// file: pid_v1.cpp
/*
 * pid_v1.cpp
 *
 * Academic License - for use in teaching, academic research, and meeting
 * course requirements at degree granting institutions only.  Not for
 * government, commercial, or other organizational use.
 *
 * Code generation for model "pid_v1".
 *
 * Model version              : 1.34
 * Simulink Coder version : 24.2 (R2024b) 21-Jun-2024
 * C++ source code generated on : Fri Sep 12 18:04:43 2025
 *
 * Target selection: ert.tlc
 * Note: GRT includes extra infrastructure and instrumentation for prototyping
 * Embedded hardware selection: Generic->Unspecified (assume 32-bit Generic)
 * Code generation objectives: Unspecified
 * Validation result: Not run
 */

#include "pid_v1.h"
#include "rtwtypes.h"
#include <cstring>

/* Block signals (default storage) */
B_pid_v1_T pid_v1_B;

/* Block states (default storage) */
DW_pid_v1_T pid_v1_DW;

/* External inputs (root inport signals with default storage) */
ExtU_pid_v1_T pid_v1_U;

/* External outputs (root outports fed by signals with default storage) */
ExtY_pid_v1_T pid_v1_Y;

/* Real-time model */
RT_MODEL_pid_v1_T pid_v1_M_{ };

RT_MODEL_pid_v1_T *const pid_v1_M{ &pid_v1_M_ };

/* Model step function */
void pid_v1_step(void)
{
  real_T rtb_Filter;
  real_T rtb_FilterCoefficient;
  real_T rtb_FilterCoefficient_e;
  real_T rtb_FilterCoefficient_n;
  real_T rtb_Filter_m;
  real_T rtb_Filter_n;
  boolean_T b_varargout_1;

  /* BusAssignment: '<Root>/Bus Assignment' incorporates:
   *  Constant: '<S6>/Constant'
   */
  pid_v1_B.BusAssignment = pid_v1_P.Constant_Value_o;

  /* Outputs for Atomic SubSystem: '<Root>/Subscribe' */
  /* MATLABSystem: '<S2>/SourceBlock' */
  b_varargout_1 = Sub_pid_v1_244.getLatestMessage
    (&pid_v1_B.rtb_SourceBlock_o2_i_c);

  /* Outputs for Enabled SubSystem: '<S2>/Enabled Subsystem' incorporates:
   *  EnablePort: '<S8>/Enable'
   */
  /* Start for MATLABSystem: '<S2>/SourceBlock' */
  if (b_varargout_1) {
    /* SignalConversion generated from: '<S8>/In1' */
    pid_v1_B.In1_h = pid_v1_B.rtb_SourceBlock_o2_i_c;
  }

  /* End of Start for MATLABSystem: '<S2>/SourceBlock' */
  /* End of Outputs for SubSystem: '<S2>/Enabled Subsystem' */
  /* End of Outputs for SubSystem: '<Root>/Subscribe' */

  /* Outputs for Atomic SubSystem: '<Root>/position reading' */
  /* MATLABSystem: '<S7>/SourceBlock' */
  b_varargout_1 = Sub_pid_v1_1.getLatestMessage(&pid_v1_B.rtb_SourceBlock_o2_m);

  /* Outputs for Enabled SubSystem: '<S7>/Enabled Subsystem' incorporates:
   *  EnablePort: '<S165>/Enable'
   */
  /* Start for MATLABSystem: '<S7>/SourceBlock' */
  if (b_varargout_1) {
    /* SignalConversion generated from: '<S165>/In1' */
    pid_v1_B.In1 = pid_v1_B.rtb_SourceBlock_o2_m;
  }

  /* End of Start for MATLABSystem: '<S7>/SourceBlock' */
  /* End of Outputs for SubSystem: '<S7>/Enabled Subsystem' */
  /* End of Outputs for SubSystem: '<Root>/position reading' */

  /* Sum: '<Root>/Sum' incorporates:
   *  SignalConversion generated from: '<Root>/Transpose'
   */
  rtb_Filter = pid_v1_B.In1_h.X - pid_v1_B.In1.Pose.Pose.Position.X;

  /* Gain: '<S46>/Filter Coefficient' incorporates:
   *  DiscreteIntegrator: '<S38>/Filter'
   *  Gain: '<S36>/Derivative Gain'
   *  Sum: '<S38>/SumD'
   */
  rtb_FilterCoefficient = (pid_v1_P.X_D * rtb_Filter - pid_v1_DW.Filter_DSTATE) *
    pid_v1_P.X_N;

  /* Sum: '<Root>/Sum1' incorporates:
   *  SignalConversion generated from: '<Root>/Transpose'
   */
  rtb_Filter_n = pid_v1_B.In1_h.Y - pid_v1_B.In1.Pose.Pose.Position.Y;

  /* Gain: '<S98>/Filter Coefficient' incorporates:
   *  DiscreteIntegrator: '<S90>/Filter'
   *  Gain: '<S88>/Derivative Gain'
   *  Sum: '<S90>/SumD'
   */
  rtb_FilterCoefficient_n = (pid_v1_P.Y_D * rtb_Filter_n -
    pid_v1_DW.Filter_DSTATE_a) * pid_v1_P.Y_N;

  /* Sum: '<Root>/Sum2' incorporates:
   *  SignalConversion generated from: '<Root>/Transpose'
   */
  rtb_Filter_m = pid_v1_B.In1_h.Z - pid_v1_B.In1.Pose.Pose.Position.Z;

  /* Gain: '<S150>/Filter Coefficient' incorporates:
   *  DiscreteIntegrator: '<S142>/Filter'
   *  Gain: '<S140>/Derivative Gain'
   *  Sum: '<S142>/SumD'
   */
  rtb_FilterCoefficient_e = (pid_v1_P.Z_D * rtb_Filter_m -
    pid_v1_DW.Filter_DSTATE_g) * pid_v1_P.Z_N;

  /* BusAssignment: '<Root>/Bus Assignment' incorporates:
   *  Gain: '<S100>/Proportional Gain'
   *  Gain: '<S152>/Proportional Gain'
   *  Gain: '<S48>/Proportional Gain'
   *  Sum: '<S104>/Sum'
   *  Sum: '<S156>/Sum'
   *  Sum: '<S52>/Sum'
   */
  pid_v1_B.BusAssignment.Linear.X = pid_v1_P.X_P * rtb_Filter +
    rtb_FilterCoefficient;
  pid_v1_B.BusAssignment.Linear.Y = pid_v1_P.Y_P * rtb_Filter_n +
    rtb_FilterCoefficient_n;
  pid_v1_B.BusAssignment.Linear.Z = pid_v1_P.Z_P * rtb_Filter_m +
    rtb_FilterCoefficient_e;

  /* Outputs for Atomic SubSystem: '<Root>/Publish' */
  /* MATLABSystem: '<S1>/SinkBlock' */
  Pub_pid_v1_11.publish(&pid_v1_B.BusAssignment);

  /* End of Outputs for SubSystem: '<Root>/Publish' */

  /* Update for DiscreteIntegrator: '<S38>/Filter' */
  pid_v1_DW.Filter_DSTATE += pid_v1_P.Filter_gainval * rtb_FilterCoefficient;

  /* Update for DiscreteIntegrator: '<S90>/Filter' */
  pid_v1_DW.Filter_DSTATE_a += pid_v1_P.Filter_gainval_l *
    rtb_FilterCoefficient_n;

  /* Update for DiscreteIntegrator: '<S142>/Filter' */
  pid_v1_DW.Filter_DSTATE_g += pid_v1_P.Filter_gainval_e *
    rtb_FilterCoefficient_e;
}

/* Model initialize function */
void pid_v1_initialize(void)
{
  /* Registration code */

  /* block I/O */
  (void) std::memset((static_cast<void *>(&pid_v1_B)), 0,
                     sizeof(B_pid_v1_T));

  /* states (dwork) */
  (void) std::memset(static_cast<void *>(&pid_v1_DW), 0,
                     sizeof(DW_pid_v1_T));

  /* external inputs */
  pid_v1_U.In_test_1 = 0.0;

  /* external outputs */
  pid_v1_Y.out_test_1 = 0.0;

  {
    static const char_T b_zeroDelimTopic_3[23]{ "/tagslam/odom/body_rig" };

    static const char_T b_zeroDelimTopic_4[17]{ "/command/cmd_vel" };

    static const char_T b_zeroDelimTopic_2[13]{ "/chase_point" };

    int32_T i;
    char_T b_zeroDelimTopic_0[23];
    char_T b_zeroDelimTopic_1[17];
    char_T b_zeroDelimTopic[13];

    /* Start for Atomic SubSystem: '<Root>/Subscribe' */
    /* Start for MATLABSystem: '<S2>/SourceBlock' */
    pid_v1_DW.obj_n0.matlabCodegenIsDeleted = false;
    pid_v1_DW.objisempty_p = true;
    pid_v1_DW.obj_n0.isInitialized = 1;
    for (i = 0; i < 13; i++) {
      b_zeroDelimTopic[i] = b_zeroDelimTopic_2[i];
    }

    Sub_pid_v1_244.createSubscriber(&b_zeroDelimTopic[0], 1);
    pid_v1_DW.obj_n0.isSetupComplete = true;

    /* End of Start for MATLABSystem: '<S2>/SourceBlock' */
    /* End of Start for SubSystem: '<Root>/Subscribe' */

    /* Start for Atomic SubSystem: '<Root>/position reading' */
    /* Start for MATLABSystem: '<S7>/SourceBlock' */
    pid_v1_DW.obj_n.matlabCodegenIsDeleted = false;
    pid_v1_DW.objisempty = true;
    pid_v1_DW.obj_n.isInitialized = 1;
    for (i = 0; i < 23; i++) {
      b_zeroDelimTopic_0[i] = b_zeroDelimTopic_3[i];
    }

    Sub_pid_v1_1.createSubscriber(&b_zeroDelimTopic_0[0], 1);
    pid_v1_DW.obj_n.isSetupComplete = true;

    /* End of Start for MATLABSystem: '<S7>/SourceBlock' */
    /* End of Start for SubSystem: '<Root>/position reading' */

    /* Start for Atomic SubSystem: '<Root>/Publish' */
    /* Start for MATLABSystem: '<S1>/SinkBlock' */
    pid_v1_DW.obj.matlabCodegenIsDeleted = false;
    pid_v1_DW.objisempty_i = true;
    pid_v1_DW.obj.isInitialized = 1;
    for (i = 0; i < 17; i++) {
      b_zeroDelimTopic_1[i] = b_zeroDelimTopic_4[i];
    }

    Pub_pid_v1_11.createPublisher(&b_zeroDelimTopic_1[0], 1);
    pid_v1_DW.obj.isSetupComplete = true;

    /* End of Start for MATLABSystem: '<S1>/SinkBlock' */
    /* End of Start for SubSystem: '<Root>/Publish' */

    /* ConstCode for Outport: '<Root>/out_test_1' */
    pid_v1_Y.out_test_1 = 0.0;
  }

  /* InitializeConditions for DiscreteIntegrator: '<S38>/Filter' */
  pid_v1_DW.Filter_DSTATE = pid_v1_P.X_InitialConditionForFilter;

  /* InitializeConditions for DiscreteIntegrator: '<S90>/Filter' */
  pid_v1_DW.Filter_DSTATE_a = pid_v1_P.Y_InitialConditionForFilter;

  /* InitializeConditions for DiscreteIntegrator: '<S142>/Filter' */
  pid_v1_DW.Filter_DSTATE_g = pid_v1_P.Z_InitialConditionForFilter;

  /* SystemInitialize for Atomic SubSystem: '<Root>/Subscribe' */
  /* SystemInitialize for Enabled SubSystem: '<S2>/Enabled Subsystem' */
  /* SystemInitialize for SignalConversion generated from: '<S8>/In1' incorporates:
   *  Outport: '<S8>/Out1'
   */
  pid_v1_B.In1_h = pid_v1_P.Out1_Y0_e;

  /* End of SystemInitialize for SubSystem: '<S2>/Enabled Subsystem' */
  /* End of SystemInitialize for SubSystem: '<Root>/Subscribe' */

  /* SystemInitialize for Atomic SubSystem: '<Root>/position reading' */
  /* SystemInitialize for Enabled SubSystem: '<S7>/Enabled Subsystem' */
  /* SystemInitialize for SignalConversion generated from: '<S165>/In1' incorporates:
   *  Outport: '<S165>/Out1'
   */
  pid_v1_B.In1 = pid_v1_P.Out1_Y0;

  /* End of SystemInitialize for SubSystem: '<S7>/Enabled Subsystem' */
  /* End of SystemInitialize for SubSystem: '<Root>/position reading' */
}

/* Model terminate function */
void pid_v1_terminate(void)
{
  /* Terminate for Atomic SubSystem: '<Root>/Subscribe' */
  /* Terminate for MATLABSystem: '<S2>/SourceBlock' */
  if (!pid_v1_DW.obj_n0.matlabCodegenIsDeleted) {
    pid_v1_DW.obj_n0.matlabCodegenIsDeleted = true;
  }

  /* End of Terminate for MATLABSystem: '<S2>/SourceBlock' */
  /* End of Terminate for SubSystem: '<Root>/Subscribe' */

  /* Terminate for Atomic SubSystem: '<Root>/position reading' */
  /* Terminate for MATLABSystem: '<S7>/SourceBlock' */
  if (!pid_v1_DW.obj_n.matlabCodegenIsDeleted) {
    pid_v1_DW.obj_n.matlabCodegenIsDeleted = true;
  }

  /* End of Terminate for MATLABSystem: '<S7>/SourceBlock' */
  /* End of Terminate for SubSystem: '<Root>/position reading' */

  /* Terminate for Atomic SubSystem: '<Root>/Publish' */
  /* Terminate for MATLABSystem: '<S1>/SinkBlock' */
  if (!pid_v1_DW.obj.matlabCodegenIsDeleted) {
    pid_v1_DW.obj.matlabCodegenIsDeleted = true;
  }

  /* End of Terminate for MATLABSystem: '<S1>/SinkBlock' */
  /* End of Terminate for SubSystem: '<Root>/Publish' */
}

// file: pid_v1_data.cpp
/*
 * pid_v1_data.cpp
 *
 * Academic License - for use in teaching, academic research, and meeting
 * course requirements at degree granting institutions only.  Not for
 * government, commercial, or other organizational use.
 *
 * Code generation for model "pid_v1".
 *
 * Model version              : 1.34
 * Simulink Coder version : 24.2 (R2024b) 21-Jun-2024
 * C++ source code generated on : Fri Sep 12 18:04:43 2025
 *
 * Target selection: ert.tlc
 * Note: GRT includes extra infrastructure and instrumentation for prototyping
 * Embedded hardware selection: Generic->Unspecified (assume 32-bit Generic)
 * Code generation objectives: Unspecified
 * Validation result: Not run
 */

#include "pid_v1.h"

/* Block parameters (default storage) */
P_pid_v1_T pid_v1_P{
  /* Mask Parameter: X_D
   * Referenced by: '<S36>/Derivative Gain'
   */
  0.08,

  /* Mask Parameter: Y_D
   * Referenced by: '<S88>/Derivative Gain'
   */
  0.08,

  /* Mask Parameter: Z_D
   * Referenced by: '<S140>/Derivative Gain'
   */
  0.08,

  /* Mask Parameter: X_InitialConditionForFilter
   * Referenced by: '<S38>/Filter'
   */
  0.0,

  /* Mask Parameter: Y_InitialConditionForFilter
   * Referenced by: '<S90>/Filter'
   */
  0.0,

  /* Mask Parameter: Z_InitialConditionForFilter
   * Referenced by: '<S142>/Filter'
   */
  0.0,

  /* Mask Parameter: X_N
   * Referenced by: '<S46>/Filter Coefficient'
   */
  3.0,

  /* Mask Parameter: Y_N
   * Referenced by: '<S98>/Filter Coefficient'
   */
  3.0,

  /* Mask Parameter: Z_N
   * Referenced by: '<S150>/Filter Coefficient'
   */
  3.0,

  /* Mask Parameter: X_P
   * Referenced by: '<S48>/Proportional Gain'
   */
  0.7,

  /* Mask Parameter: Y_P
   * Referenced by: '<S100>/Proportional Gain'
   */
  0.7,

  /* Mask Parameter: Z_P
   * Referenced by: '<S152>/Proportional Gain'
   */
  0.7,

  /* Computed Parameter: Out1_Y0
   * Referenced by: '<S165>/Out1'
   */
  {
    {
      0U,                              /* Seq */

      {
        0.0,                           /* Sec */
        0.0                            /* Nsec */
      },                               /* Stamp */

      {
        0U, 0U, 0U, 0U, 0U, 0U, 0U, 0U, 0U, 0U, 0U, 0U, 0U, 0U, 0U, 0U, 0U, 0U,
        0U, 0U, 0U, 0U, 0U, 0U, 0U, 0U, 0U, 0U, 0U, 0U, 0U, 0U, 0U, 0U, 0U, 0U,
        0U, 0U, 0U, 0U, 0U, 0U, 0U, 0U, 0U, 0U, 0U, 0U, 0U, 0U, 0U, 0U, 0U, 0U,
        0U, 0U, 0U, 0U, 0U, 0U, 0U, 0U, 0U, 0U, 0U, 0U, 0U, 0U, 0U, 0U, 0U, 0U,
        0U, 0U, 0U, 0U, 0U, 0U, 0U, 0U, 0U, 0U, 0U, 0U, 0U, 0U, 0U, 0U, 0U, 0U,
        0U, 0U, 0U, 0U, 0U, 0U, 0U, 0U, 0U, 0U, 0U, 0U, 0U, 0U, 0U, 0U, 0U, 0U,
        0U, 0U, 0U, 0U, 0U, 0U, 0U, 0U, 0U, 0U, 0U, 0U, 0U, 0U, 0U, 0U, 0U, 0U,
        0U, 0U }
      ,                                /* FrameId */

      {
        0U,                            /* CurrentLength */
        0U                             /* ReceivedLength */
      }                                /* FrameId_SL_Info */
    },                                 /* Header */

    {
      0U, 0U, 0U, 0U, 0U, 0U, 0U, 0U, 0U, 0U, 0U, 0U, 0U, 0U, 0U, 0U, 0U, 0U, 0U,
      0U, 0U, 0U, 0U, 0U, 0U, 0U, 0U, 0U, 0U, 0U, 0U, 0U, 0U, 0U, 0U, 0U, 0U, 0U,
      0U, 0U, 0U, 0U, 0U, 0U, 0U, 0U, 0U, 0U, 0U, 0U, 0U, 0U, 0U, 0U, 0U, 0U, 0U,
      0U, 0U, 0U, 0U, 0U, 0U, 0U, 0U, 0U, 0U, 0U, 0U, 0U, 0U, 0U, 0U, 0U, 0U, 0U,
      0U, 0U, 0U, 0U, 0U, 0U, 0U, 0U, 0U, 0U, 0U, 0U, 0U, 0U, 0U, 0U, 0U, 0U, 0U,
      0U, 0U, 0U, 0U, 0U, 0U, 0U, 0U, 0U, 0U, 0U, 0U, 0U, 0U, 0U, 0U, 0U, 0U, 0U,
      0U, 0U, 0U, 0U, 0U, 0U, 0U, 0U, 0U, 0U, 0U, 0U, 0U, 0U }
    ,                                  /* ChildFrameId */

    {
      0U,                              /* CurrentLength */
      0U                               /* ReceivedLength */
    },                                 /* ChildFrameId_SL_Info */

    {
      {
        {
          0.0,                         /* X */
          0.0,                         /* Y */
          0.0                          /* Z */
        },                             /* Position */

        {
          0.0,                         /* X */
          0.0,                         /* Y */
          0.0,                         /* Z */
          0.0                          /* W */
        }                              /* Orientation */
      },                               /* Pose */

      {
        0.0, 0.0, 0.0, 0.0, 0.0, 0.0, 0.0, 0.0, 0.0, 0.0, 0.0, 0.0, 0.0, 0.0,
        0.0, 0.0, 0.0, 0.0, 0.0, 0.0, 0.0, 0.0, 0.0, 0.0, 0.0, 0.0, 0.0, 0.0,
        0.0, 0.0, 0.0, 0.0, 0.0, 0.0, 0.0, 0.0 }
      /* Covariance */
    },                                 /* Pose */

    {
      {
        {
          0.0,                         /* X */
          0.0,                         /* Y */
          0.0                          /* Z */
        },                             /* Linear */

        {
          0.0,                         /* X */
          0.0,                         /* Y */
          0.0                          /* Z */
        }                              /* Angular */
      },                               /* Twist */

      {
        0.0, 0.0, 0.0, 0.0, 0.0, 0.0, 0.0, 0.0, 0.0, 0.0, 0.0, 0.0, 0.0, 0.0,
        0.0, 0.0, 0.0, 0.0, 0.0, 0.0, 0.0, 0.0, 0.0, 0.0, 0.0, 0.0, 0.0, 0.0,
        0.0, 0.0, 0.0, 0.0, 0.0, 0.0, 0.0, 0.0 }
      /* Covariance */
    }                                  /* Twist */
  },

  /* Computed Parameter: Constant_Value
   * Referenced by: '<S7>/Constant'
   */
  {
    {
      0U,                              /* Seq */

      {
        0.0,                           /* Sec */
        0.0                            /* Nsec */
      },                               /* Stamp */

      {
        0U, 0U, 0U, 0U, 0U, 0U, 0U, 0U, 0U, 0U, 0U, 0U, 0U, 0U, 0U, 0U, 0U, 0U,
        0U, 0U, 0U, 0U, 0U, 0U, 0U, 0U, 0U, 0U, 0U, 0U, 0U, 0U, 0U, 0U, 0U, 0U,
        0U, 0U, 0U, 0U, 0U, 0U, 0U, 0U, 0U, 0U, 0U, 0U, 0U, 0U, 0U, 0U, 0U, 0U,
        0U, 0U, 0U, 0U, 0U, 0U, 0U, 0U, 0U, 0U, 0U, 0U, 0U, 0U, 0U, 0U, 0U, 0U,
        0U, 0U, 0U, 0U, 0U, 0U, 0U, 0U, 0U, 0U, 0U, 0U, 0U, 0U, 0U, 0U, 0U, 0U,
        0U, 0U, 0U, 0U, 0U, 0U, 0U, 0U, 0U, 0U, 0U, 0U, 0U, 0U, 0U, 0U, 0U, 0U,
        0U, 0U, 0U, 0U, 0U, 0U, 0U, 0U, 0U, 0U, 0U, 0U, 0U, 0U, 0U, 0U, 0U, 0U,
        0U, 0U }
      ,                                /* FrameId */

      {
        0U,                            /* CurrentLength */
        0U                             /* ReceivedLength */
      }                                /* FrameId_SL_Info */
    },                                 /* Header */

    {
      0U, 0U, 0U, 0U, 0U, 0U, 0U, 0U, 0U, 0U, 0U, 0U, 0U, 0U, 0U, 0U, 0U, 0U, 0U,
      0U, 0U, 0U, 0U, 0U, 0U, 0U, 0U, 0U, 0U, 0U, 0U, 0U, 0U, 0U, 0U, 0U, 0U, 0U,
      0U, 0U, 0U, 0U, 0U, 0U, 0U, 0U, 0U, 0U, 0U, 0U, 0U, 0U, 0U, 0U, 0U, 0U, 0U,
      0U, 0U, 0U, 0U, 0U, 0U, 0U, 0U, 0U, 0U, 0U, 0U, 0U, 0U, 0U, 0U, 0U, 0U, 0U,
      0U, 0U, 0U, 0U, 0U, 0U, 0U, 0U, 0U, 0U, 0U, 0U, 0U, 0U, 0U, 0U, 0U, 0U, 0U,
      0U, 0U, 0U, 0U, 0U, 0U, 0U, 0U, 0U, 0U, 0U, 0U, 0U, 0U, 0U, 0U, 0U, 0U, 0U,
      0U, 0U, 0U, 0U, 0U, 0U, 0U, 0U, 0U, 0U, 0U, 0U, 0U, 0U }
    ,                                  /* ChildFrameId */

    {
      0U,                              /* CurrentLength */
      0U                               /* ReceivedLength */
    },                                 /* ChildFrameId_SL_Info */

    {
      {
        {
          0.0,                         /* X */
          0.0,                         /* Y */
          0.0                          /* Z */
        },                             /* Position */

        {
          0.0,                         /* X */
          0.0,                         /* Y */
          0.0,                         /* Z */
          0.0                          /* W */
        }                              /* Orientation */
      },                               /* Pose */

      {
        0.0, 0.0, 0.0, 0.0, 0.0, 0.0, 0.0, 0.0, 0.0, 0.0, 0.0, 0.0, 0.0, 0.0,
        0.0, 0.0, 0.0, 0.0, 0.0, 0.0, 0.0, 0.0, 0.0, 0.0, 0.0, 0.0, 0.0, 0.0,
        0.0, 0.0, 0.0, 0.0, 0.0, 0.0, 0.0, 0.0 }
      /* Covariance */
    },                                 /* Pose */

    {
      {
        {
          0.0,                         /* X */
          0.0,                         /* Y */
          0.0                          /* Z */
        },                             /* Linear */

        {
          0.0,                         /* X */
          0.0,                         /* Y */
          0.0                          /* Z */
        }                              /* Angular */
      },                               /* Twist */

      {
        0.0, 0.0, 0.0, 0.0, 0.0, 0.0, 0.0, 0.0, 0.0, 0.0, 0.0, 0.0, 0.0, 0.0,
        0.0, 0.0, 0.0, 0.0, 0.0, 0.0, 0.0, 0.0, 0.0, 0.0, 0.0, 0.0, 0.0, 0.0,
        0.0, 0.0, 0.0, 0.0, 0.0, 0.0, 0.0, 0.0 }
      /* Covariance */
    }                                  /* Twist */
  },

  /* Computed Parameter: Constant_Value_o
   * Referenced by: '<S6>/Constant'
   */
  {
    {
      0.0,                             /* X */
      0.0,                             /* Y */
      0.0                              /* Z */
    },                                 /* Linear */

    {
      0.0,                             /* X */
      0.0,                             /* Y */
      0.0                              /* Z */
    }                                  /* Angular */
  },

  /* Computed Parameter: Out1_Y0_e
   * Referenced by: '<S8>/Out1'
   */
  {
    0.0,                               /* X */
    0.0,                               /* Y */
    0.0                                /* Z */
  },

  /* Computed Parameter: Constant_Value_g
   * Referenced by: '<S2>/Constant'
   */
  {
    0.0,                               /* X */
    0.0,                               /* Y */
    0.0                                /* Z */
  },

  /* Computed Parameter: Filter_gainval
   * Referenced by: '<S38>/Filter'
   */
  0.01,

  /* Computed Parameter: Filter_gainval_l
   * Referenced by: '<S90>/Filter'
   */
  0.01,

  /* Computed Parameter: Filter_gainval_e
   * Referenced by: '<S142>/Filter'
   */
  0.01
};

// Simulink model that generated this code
simulink model "pid_v1"  (R2024b)
settings: Solver=FixedStepAuto  StartTime=0.0  StopTime=inf  RelTol=1e-3
model workspace (MAT data in the model file):
  ROSControlClassName_ = 'ControllerHost'
  ROSControlDynamicReconfTable_ : object (value not decoded)
  ROSControlInportTable_ : string (value not decoded)
  ROSControlOutportTable_ : string (value not decoded)
undefined symbols (not defined in the file): Linear
libraries: robotlib x4, slpidlib x3

== system pid_v1 ==
  In_test_1 : Inport
  Bus Assignment : BusAssignment  AssignedSignals=Linear.X,Linear.Y,Linear.Z
  Bus Selector : BusSelector  DialogController=Simulink.DDGSource_BusSelector  OutputSignals=Pose.Pose.Position.X,Pose.Pose.Position.Y,Pose.Pose.Position.Z
  Bus Selector1 : BusSelector  OutputSignals=X,Y,Z  OutputAsBus=on
  Publish : robotlib/Publish  topicSource=Select from ROS network  topic=/command/cmd_vel  messageType=geometry_msgs/Twist  legacyBusStruct=off  messageQueueLength=1
  Selector : Selector  IndexMode=Zero-based  InputPortWidth=3  IndexOptions=Index vector (dialog)  Indices=[0]  OutputSizes=1
  Selector1 : Selector  IndexMode=Zero-based  InputPortWidth=3  IndexOptions=Index vector (dialog)  Indices=[1]  OutputSizes=1
  Selector2 : Selector  IndexMode=Zero-based  InputPortWidth=3  IndexOptions=Index vector (dialog)  Indices=[2]  OutputSizes=1
  Subscribe : robotlib/Subscribe  topicSource=Specify your own  topic=/chase_point  messageType=geometry_msgs/Point  SampleTime=-1  legacyBusStruct=off  messageQueueLength=1
  Sum : Sum  Inputs=|+-
  Sum1 : Sum  Inputs=|+-
  Sum2 : Sum  Inputs=|+-
  Transpose : Math  Operator=transpose
  X : slpidlib/PID Controller  Controller=PD  Form=Parallel  TimeDomain=Discrete-time  UseExternalTs=off  SampleTime=0.01  IntegratorMethod=Forward Euler  FilterMethod=Forward Euler  ControllerParametersSource=internal  P=0.7  I=0  UseKiTs=off  D=0.08  UseExternalDerivativeSource=off  N=3  UseFilter=on  TunerSelectOption=Frequency Response Based  InitialConditionSource=internal  InitialConditionForIntegrator=0  InitialConditionForFilter=0  DifferentiatorICPrevScaledInput=0  ExternalReset=none  TrackingMode=off  Kt=1  LimitOutput=off  SatLimitsSource=internal  UpperSaturationLimit=1  LowerSaturationLimit=-1  LinearizeAsGain=on  AntiWindupMode=none  Kb=1  LimitIntegrator=off  UpperIntegratorSaturationLimit=inf  LowerIntegratorSaturationLimit=-inf  POutMin=[]  POutMax=[]  IOutMin=[]  IOutMax=[]  DOutMin=[]  DOutMax=[]  NOutMin=[]  NOutMax=[]  SumOutMin=[]  SumOutMax=[]  SaturationOutMin=[]  SaturationOutMax=[]  PParamMin=[]  PParamMax=[]  IParamMin=[]  IParamMax=[]  DParamMin=[]  DParamMax=[]  NParamMin=[]  NParamMax=[]  KbParamMin=[]  KbParamMax=[]  KtParamMin=[]  KtParamMax=[]  KbOutMin=[]  KbOutMax=[]  KtOutMin=[]  KtOutMax=[]  IntegratorOutMin=[]  IntegratorOutMax=[]  FilterOutMin=[]  FilterOutMax=[]  SumI1OutMin=[]  SumI1OutMax=[]  SumI2OutMin=[]  SumI2OutMax=[]  SumI3OutMin=[]  SumI3OutMax=[]  SumI4OutMin=[]  SumI4OutMax=[]  SumDOutMin=[]  SumDOutMax=[]  DifferentiatorOutMin=[]  DifferentiatorOutMax=[]  FilterDiffOutCoefMin=[]  FilterDiffOutCoefMax=[]  ReciprocalOutMin=[]  ReciprocalOutMax=[]  SumDenOutMin=[]  SumDenOutMax=[]  SumNumOutMin=[]  SumNumOutMax=[]  DivideOutMin=[]  DivideOutMax=[]  UdiffTsProdOutMin=[]  UdiffTsProdOutMax=[]  NTsProdOutMin=[]  NTsProdOutMax=[]  UintegralTsProdOutMin=[]  UintegralTsProdOutMax=[]  UngainTsProdOutMin=[]  UngainTsProdOutMax=[]  ClampingZeroOutDataTypeStr=Inherit: Inherit via back propagation  ClampingZeroOutMin=[]  ClampingZeroOutMax=[]  FilterDenConstantOutDataTypeStr=Inherit: Inherit via back propagation  FilterDenConstantOutMin=[]  FilterDenConstantOutMax=[]  PCopyOutDataTypeStr=Inherit: Inherit via back propagation  PCopyOutMin=[]  PCopyOutMax=[]  NCopyOutDataTypeStr=Inherit: Inherit via back propagation  NCopyOutMin=[]  NCopyOutMax=[]  IntegratorContinuousStateAttributes=''  IntegratorStateMustResolveToSignalObject=off  IntegratorRTWStateStorageClass=Auto  FilterContinuousStateAttributes=''  FilterStateMustResolveToSignalObject=off  FilterRTWStateStorageClass=Auto  ParallelPVariant=InternalParameters  IdealPVariant=Disabled  IVariant=Disabled  DVariant=InternalParameters  IntegratorVariant=Disabled  SatVariant=Disabled  AWVariant=Disabled  PCopyVariant=Disabled  TRVariant=Disabled  FdbkBlocksVariant=Forward  IdealPFdbkVariant=Disabled  SatFdbkVariant=Disabled  DerivativeFilterVariant=ForwardEulerFilter  NVariant=InternalParameters  NCopyVariant=Disabled  FilterICVariant=InternalICsFilter  IntegratorICVariant=Disabled  ExternalResetVariant=Disabled  TRSumVariant=Passthrough  SumFdbkVariant=Disabled  SumVariant=Sum_PD  TsampFilterVariant=InternalTs  TsampNgainVariant=Passthrough  TsampIntegralVariant=Disabled_SignalSpec  ExternalSaturationOutDataTypeStr=Inherit: Same as second input  DerivativeSourceVariant=ErrorSignal  PreIntVariant=InternalPreInt
  Y : slpidlib/PID Controller  Controller=PD  Form=Parallel  TimeDomain=Discrete-time  UseExternalTs=off  SampleTime=0.01  IntegratorMethod=Forward Euler  FilterMethod=Forward Euler  ControllerParametersSource=internal  P=0.7  I=0  UseKiTs=off  D=0.08  UseExternalDerivativeSource=off  N=3  UseFilter=on  TunerSelectOption=Frequency Response Based  InitialConditionSource=internal  InitialConditionForIntegrator=0  InitialConditionForFilter=0  DifferentiatorICPrevScaledInput=0  ExternalReset=none  TrackingMode=off  Kt=1  LimitOutput=off  SatLimitsSource=internal  UpperSaturationLimit=1  LowerSaturationLimit=-1  LinearizeAsGain=on  AntiWindupMode=none  Kb=1  LimitIntegrator=off  UpperIntegratorSaturationLimit=inf  LowerIntegratorSaturationLimit=-inf  POutMin=[]  POutMax=[]  IOutMin=[]  IOutMax=[]  DOutMin=[]  DOutMax=[]  NOutMin=[]  NOutMax=[]  SumOutMin=[]  SumOutMax=[]  SaturationOutMin=[]  SaturationOutMax=[]  PParamMin=[]  PParamMax=[]  IParamMin=[]  IParamMax=[]  DParamMin=[]  DParamMax=[]  NParamMin=[]  NParamMax=[]  KbParamMin=[]  KbParamMax=[]  KtParamMin=[]  KtParamMax=[]  KbOutMin=[]  KbOutMax=[]  KtOutMin=[]  KtOutMax=[]  IntegratorOutMin=[]  IntegratorOutMax=[]  FilterOutMin=[]  FilterOutMax=[]  SumI1OutMin=[]  SumI1OutMax=[]  SumI2OutMin=[]  SumI2OutMax=[]  SumI3OutMin=[]  SumI3OutMax=[]  SumI4OutMin=[]  SumI4OutMax=[]  SumDOutMin=[]  SumDOutMax=[]  DifferentiatorOutMin=[]  DifferentiatorOutMax=[]  FilterDiffOutCoefMin=[]  FilterDiffOutCoefMax=[]  ReciprocalOutMin=[]  ReciprocalOutMax=[]  SumDenOutMin=[]  SumDenOutMax=[]  SumNumOutMin=[]  SumNumOutMax=[]  DivideOutMin=[]  DivideOutMax=[]  UdiffTsProdOutMin=[]  UdiffTsProdOutMax=[]  NTsProdOutMin=[]  NTsProdOutMax=[]  UintegralTsProdOutMin=[]  UintegralTsProdOutMax=[]  UngainTsProdOutMin=[]  UngainTsProdOutMax=[]  ClampingZeroOutDataTypeStr=Inherit: Inherit via back propagation  ClampingZeroOutMin=[]  ClampingZeroOutMax=[]  FilterDenConstantOutDataTypeStr=Inherit: Inherit via back propagation  FilterDenConstantOutMin=[]  FilterDenConstantOutMax=[]  PCopyOutDataTypeStr=Inherit: Inherit via back propagation  PCopyOutMin=[]  PCopyOutMax=[]  NCopyOutDataTypeStr=Inherit: Inherit via back propagation  NCopyOutMin=[]  NCopyOutMax=[]  IntegratorContinuousStateAttributes=''  IntegratorStateMustResolveToSignalObject=off  IntegratorRTWStateStorageClass=Auto  FilterContinuousStateAttributes=''  FilterStateMustResolveToSignalObject=off  FilterRTWStateStorageClass=Auto  ParallelPVariant=InternalParameters  IdealPVariant=Disabled  IVariant=Disabled  DVariant=InternalParameters  IntegratorVariant=Disabled  SatVariant=Disabled  AWVariant=Disabled  PCopyVariant=Disabled  TRVariant=Disabled  FdbkBlocksVariant=Forward  IdealPFdbkVariant=Disabled  SatFdbkVariant=Disabled  DerivativeFilterVariant=ForwardEulerFilter  NVariant=InternalParameters  NCopyVariant=Disabled  FilterICVariant=InternalICsFilter  IntegratorICVariant=Disabled  ExternalResetVariant=Disabled  TRSumVariant=Passthrough  SumFdbkVariant=Disabled  SumVariant=Sum_PD  TsampFilterVariant=InternalTs  TsampNgainVariant=Passthrough  TsampIntegralVariant=Disabled_SignalSpec  ExternalSaturationOutDataTypeStr=Inherit: Same as second input  DerivativeSourceVariant=ErrorSignal  PreIntVariant=InternalPreInt
  Z : slpidlib/PID Controller  Controller=PD  Form=Parallel  TimeDomain=Discrete-time  UseExternalTs=off  SampleTime=0.01  IntegratorMethod=Forward Euler  FilterMethod=Forward Euler  ControllerParametersSource=internal  P=0.7  I=0  UseKiTs=off  D=0.08  UseExternalDerivativeSource=off  N=3  UseFilter=on  TunerSelectOption=Frequency Response Based  InitialConditionSource=internal  InitialConditionForIntegrator=0  InitialConditionForFilter=0  DifferentiatorICPrevScaledInput=0  ExternalReset=none  TrackingMode=off  Kt=1  LimitOutput=off  SatLimitsSource=internal  UpperSaturationLimit=1  LowerSaturationLimit=-1  LinearizeAsGain=on  AntiWindupMode=none  Kb=1  LimitIntegrator=off  UpperIntegratorSaturationLimit=inf  LowerIntegratorSaturationLimit=-inf  POutMin=[]  POutMax=[]  IOutMin=[]  IOutMax=[]  DOutMin=[]  DOutMax=[]  NOutMin=[]  NOutMax=[]  SumOutMin=[]  SumOutMax=[]  SaturationOutMin=[]  SaturationOutMax=[]  PParamMin=[]  PParamMax=[]  IParamMin=[]  IParamMax=[]  DParamMin=[]  DParamMax=[]  NParamMin=[]  NParamMax=[]  KbParamMin=[]  KbParamMax=[]  KtParamMin=[]  KtParamMax=[]  KbOutMin=[]  KbOutMax=[]  KtOutMin=[]  KtOutMax=[]  IntegratorOutMin=[]  IntegratorOutMax=[]  FilterOutMin=[]  FilterOutMax=[]  SumI1OutMin=[]  SumI1OutMax=[]  SumI2OutMin=[]  SumI2OutMax=[]  SumI3OutMin=[]  SumI3OutMax=[]  SumI4OutMin=[]  SumI4OutMax=[]  SumDOutMin=[]  SumDOutMax=[]  DifferentiatorOutMin=[]  DifferentiatorOutMax=[]  FilterDiffOutCoefMin=[]  FilterDiffOutCoefMax=[]  ReciprocalOutMin=[]  ReciprocalOutMax=[]  SumDenOutMin=[]  SumDenOutMax=[]  SumNumOutMin=[]  SumNumOutMax=[]  DivideOutMin=[]  DivideOutMax=[]  UdiffTsProdOutMin=[]  UdiffTsProdOutMax=[]  NTsProdOutMin=[]  NTsProdOutMax=[]  UintegralTsProdOutMin=[]  UintegralTsProdOutMax=[]  UngainTsProdOutMin=[]  UngainTsProdOutMax=[]  ClampingZeroOutDataTypeStr=Inherit: Inherit via back propagation  ClampingZeroOutMin=[]  ClampingZeroOutMax=[]  FilterDenConstantOutDataTypeStr=Inherit: Inherit via back propagation  FilterDenConstantOutMin=[]  FilterDenConstantOutMax=[]  PCopyOutDataTypeStr=Inherit: Inherit via back propagation  PCopyOutMin=[]  PCopyOutMax=[]  NCopyOutDataTypeStr=Inherit: Inherit via back propagation  NCopyOutMin=[]  NCopyOutMax=[]  IntegratorContinuousStateAttributes=''  IntegratorStateMustResolveToSignalObject=off  IntegratorRTWStateStorageClass=Auto  FilterContinuousStateAttributes=''  FilterStateMustResolveToSignalObject=off  FilterRTWStateStorageClass=Auto  ParallelPVariant=InternalParameters  IdealPVariant=Disabled  IVariant=Disabled  DVariant=InternalParameters  IntegratorVariant=Disabled  SatVariant=Disabled  AWVariant=Disabled  PCopyVariant=Disabled  TRVariant=Disabled  FdbkBlocksVariant=Forward  IdealPFdbkVariant=Disabled  SatFdbkVariant=Disabled  DerivativeFilterVariant=ForwardEulerFilter  NVariant=InternalParameters  NCopyVariant=Disabled  FilterICVariant=InternalICsFilter  IntegratorICVariant=Disabled  ExternalResetVariant=Disabled  TRSumVariant=Passthrough  SumFdbkVariant=Disabled  SumVariant=Sum_PD  TsampFilterVariant=InternalTs  TsampNgainVariant=Passthrough  TsampIntegralVariant=Disabled_SignalSpec  ExternalSaturationOutDataTypeStr=Inherit: Same as second input  DerivativeSourceVariant=ErrorSignal  PreIntVariant=InternalPreInt
  control output : robotlib/Blank Message  messageClass=Message  entityType=geometry_msgs/Twist  messageType=geometry_msgs/Twist  SampleTime=inf  legacyBusStruct=off
  position reading : robotlib/Subscribe  topicSource=Select from ROS network  topic=/tagslam/odom/body_rig  messageType=nav_msgs/Odometry  SampleTime=-1  legacyBusStruct=off  messageQueueLength=1
  out_test_1 : Outport
  wires:
  control output/1 -> Bus Assignment/1
  Bus Assignment/1 -> Publish/1
  Sum/1 -> X/1
  Sum1/1 -> Y/1
  Sum2/1 -> Z/1
  Selector1/1 -> Sum1/1  "target point y"
  Selector2/1 -> Sum2/1  "target point z"
  Selector/1 -> Sum/1  "target point x"
  Z/1 -> Bus Assignment/4  "Vz"
  X/1 -> Bus Assignment/2  "Vx"
  Y/1 -> Bus Assignment/3  "Vy"
  Transpose/1 -> Selector1/1, Selector/1, Selector2/1
  Bus Selector1/1 -> Transpose/1
  Bus Selector/3 -> Sum2/2  "<Z>"
  Bus Selector/2 -> Sum1/2  "<Y>"
  Bus Selector/1 -> Sum/2  "<X>"
  Subscribe/2 -> Bus Selector1/1
  position reading/2 -> Bus Selector/1
